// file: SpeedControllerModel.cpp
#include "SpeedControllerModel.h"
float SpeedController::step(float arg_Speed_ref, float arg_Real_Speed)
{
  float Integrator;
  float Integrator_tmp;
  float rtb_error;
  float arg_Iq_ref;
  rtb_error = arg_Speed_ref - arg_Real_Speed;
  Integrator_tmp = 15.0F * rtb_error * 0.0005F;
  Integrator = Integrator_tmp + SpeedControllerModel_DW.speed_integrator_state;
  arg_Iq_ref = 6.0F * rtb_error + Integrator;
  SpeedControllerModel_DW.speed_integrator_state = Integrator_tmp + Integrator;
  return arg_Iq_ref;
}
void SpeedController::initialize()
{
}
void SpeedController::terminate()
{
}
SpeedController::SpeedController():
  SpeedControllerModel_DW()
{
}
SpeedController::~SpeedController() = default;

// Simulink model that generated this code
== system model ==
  Speed_ref : Inport
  Real_Speed : Inport
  Iq_ref : Outport  <- 1: PIDController#1
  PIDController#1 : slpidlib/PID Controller  Controller=PI  Form=Parallel  TimeDomain=Discrete-time  IntegratorMethod=Trapezoidal  P=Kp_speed  I=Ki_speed  D=0  N=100  InitialConditionForIntegrator=0  ExternalReset=none  LimitOutput=off  UpperSaturationLimit=inf  LowerSaturationLimit=-inf  <- 1: Sum#1
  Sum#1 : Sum  Inputs=+-  <- 1: Speed_ref, 2: Real_Speed
